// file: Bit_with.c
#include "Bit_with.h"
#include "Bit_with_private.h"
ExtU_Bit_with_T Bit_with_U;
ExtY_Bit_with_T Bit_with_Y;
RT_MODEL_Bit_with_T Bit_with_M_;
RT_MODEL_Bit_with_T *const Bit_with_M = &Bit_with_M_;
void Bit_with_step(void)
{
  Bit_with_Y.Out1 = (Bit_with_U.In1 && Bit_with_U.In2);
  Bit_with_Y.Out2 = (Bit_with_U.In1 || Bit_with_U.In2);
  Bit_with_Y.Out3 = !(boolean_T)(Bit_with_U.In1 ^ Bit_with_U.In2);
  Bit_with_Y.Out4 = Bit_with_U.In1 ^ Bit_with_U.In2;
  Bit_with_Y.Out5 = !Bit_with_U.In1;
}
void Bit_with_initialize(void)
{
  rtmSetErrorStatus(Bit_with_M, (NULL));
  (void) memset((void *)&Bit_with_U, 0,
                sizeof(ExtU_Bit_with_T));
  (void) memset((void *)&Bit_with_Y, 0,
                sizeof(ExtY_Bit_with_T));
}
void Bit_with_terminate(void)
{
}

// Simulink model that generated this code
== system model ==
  In2 : Inport
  In1 : Inport
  Out1 : Outport  <- 1: BitwiseOperator#1
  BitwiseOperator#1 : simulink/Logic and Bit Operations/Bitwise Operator  logicop=AND  BitMask=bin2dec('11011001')  <- 1: In1, 2: In2
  Out2 : Outport  <- 1: BitwiseOperator#2
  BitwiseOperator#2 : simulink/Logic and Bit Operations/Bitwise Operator  logicop=OR  BitMask=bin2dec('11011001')  <- 1: In1, 2: In2
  Out3 : Outport  <- 1: BitwiseOperator#3
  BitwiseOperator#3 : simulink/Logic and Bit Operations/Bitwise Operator  logicop=NOT  BitMask=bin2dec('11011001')  <- 1: BitwiseOperator#4
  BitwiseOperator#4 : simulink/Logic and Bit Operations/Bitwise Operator  logicop=XOR  BitMask=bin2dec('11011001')  <- 1: In1, 2: In2
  Out4 : Outport  <- 1: BitwiseOperator#5
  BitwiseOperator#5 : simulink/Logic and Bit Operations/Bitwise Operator  logicop=XOR  BitMask=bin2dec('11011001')  <- 1: In1, 2: In2
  Out5 : Outport  <- 1: BitwiseOperator#6
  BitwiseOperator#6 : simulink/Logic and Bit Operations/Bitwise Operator  logicop=NOT  BitMask=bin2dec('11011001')  <- 1: In1
